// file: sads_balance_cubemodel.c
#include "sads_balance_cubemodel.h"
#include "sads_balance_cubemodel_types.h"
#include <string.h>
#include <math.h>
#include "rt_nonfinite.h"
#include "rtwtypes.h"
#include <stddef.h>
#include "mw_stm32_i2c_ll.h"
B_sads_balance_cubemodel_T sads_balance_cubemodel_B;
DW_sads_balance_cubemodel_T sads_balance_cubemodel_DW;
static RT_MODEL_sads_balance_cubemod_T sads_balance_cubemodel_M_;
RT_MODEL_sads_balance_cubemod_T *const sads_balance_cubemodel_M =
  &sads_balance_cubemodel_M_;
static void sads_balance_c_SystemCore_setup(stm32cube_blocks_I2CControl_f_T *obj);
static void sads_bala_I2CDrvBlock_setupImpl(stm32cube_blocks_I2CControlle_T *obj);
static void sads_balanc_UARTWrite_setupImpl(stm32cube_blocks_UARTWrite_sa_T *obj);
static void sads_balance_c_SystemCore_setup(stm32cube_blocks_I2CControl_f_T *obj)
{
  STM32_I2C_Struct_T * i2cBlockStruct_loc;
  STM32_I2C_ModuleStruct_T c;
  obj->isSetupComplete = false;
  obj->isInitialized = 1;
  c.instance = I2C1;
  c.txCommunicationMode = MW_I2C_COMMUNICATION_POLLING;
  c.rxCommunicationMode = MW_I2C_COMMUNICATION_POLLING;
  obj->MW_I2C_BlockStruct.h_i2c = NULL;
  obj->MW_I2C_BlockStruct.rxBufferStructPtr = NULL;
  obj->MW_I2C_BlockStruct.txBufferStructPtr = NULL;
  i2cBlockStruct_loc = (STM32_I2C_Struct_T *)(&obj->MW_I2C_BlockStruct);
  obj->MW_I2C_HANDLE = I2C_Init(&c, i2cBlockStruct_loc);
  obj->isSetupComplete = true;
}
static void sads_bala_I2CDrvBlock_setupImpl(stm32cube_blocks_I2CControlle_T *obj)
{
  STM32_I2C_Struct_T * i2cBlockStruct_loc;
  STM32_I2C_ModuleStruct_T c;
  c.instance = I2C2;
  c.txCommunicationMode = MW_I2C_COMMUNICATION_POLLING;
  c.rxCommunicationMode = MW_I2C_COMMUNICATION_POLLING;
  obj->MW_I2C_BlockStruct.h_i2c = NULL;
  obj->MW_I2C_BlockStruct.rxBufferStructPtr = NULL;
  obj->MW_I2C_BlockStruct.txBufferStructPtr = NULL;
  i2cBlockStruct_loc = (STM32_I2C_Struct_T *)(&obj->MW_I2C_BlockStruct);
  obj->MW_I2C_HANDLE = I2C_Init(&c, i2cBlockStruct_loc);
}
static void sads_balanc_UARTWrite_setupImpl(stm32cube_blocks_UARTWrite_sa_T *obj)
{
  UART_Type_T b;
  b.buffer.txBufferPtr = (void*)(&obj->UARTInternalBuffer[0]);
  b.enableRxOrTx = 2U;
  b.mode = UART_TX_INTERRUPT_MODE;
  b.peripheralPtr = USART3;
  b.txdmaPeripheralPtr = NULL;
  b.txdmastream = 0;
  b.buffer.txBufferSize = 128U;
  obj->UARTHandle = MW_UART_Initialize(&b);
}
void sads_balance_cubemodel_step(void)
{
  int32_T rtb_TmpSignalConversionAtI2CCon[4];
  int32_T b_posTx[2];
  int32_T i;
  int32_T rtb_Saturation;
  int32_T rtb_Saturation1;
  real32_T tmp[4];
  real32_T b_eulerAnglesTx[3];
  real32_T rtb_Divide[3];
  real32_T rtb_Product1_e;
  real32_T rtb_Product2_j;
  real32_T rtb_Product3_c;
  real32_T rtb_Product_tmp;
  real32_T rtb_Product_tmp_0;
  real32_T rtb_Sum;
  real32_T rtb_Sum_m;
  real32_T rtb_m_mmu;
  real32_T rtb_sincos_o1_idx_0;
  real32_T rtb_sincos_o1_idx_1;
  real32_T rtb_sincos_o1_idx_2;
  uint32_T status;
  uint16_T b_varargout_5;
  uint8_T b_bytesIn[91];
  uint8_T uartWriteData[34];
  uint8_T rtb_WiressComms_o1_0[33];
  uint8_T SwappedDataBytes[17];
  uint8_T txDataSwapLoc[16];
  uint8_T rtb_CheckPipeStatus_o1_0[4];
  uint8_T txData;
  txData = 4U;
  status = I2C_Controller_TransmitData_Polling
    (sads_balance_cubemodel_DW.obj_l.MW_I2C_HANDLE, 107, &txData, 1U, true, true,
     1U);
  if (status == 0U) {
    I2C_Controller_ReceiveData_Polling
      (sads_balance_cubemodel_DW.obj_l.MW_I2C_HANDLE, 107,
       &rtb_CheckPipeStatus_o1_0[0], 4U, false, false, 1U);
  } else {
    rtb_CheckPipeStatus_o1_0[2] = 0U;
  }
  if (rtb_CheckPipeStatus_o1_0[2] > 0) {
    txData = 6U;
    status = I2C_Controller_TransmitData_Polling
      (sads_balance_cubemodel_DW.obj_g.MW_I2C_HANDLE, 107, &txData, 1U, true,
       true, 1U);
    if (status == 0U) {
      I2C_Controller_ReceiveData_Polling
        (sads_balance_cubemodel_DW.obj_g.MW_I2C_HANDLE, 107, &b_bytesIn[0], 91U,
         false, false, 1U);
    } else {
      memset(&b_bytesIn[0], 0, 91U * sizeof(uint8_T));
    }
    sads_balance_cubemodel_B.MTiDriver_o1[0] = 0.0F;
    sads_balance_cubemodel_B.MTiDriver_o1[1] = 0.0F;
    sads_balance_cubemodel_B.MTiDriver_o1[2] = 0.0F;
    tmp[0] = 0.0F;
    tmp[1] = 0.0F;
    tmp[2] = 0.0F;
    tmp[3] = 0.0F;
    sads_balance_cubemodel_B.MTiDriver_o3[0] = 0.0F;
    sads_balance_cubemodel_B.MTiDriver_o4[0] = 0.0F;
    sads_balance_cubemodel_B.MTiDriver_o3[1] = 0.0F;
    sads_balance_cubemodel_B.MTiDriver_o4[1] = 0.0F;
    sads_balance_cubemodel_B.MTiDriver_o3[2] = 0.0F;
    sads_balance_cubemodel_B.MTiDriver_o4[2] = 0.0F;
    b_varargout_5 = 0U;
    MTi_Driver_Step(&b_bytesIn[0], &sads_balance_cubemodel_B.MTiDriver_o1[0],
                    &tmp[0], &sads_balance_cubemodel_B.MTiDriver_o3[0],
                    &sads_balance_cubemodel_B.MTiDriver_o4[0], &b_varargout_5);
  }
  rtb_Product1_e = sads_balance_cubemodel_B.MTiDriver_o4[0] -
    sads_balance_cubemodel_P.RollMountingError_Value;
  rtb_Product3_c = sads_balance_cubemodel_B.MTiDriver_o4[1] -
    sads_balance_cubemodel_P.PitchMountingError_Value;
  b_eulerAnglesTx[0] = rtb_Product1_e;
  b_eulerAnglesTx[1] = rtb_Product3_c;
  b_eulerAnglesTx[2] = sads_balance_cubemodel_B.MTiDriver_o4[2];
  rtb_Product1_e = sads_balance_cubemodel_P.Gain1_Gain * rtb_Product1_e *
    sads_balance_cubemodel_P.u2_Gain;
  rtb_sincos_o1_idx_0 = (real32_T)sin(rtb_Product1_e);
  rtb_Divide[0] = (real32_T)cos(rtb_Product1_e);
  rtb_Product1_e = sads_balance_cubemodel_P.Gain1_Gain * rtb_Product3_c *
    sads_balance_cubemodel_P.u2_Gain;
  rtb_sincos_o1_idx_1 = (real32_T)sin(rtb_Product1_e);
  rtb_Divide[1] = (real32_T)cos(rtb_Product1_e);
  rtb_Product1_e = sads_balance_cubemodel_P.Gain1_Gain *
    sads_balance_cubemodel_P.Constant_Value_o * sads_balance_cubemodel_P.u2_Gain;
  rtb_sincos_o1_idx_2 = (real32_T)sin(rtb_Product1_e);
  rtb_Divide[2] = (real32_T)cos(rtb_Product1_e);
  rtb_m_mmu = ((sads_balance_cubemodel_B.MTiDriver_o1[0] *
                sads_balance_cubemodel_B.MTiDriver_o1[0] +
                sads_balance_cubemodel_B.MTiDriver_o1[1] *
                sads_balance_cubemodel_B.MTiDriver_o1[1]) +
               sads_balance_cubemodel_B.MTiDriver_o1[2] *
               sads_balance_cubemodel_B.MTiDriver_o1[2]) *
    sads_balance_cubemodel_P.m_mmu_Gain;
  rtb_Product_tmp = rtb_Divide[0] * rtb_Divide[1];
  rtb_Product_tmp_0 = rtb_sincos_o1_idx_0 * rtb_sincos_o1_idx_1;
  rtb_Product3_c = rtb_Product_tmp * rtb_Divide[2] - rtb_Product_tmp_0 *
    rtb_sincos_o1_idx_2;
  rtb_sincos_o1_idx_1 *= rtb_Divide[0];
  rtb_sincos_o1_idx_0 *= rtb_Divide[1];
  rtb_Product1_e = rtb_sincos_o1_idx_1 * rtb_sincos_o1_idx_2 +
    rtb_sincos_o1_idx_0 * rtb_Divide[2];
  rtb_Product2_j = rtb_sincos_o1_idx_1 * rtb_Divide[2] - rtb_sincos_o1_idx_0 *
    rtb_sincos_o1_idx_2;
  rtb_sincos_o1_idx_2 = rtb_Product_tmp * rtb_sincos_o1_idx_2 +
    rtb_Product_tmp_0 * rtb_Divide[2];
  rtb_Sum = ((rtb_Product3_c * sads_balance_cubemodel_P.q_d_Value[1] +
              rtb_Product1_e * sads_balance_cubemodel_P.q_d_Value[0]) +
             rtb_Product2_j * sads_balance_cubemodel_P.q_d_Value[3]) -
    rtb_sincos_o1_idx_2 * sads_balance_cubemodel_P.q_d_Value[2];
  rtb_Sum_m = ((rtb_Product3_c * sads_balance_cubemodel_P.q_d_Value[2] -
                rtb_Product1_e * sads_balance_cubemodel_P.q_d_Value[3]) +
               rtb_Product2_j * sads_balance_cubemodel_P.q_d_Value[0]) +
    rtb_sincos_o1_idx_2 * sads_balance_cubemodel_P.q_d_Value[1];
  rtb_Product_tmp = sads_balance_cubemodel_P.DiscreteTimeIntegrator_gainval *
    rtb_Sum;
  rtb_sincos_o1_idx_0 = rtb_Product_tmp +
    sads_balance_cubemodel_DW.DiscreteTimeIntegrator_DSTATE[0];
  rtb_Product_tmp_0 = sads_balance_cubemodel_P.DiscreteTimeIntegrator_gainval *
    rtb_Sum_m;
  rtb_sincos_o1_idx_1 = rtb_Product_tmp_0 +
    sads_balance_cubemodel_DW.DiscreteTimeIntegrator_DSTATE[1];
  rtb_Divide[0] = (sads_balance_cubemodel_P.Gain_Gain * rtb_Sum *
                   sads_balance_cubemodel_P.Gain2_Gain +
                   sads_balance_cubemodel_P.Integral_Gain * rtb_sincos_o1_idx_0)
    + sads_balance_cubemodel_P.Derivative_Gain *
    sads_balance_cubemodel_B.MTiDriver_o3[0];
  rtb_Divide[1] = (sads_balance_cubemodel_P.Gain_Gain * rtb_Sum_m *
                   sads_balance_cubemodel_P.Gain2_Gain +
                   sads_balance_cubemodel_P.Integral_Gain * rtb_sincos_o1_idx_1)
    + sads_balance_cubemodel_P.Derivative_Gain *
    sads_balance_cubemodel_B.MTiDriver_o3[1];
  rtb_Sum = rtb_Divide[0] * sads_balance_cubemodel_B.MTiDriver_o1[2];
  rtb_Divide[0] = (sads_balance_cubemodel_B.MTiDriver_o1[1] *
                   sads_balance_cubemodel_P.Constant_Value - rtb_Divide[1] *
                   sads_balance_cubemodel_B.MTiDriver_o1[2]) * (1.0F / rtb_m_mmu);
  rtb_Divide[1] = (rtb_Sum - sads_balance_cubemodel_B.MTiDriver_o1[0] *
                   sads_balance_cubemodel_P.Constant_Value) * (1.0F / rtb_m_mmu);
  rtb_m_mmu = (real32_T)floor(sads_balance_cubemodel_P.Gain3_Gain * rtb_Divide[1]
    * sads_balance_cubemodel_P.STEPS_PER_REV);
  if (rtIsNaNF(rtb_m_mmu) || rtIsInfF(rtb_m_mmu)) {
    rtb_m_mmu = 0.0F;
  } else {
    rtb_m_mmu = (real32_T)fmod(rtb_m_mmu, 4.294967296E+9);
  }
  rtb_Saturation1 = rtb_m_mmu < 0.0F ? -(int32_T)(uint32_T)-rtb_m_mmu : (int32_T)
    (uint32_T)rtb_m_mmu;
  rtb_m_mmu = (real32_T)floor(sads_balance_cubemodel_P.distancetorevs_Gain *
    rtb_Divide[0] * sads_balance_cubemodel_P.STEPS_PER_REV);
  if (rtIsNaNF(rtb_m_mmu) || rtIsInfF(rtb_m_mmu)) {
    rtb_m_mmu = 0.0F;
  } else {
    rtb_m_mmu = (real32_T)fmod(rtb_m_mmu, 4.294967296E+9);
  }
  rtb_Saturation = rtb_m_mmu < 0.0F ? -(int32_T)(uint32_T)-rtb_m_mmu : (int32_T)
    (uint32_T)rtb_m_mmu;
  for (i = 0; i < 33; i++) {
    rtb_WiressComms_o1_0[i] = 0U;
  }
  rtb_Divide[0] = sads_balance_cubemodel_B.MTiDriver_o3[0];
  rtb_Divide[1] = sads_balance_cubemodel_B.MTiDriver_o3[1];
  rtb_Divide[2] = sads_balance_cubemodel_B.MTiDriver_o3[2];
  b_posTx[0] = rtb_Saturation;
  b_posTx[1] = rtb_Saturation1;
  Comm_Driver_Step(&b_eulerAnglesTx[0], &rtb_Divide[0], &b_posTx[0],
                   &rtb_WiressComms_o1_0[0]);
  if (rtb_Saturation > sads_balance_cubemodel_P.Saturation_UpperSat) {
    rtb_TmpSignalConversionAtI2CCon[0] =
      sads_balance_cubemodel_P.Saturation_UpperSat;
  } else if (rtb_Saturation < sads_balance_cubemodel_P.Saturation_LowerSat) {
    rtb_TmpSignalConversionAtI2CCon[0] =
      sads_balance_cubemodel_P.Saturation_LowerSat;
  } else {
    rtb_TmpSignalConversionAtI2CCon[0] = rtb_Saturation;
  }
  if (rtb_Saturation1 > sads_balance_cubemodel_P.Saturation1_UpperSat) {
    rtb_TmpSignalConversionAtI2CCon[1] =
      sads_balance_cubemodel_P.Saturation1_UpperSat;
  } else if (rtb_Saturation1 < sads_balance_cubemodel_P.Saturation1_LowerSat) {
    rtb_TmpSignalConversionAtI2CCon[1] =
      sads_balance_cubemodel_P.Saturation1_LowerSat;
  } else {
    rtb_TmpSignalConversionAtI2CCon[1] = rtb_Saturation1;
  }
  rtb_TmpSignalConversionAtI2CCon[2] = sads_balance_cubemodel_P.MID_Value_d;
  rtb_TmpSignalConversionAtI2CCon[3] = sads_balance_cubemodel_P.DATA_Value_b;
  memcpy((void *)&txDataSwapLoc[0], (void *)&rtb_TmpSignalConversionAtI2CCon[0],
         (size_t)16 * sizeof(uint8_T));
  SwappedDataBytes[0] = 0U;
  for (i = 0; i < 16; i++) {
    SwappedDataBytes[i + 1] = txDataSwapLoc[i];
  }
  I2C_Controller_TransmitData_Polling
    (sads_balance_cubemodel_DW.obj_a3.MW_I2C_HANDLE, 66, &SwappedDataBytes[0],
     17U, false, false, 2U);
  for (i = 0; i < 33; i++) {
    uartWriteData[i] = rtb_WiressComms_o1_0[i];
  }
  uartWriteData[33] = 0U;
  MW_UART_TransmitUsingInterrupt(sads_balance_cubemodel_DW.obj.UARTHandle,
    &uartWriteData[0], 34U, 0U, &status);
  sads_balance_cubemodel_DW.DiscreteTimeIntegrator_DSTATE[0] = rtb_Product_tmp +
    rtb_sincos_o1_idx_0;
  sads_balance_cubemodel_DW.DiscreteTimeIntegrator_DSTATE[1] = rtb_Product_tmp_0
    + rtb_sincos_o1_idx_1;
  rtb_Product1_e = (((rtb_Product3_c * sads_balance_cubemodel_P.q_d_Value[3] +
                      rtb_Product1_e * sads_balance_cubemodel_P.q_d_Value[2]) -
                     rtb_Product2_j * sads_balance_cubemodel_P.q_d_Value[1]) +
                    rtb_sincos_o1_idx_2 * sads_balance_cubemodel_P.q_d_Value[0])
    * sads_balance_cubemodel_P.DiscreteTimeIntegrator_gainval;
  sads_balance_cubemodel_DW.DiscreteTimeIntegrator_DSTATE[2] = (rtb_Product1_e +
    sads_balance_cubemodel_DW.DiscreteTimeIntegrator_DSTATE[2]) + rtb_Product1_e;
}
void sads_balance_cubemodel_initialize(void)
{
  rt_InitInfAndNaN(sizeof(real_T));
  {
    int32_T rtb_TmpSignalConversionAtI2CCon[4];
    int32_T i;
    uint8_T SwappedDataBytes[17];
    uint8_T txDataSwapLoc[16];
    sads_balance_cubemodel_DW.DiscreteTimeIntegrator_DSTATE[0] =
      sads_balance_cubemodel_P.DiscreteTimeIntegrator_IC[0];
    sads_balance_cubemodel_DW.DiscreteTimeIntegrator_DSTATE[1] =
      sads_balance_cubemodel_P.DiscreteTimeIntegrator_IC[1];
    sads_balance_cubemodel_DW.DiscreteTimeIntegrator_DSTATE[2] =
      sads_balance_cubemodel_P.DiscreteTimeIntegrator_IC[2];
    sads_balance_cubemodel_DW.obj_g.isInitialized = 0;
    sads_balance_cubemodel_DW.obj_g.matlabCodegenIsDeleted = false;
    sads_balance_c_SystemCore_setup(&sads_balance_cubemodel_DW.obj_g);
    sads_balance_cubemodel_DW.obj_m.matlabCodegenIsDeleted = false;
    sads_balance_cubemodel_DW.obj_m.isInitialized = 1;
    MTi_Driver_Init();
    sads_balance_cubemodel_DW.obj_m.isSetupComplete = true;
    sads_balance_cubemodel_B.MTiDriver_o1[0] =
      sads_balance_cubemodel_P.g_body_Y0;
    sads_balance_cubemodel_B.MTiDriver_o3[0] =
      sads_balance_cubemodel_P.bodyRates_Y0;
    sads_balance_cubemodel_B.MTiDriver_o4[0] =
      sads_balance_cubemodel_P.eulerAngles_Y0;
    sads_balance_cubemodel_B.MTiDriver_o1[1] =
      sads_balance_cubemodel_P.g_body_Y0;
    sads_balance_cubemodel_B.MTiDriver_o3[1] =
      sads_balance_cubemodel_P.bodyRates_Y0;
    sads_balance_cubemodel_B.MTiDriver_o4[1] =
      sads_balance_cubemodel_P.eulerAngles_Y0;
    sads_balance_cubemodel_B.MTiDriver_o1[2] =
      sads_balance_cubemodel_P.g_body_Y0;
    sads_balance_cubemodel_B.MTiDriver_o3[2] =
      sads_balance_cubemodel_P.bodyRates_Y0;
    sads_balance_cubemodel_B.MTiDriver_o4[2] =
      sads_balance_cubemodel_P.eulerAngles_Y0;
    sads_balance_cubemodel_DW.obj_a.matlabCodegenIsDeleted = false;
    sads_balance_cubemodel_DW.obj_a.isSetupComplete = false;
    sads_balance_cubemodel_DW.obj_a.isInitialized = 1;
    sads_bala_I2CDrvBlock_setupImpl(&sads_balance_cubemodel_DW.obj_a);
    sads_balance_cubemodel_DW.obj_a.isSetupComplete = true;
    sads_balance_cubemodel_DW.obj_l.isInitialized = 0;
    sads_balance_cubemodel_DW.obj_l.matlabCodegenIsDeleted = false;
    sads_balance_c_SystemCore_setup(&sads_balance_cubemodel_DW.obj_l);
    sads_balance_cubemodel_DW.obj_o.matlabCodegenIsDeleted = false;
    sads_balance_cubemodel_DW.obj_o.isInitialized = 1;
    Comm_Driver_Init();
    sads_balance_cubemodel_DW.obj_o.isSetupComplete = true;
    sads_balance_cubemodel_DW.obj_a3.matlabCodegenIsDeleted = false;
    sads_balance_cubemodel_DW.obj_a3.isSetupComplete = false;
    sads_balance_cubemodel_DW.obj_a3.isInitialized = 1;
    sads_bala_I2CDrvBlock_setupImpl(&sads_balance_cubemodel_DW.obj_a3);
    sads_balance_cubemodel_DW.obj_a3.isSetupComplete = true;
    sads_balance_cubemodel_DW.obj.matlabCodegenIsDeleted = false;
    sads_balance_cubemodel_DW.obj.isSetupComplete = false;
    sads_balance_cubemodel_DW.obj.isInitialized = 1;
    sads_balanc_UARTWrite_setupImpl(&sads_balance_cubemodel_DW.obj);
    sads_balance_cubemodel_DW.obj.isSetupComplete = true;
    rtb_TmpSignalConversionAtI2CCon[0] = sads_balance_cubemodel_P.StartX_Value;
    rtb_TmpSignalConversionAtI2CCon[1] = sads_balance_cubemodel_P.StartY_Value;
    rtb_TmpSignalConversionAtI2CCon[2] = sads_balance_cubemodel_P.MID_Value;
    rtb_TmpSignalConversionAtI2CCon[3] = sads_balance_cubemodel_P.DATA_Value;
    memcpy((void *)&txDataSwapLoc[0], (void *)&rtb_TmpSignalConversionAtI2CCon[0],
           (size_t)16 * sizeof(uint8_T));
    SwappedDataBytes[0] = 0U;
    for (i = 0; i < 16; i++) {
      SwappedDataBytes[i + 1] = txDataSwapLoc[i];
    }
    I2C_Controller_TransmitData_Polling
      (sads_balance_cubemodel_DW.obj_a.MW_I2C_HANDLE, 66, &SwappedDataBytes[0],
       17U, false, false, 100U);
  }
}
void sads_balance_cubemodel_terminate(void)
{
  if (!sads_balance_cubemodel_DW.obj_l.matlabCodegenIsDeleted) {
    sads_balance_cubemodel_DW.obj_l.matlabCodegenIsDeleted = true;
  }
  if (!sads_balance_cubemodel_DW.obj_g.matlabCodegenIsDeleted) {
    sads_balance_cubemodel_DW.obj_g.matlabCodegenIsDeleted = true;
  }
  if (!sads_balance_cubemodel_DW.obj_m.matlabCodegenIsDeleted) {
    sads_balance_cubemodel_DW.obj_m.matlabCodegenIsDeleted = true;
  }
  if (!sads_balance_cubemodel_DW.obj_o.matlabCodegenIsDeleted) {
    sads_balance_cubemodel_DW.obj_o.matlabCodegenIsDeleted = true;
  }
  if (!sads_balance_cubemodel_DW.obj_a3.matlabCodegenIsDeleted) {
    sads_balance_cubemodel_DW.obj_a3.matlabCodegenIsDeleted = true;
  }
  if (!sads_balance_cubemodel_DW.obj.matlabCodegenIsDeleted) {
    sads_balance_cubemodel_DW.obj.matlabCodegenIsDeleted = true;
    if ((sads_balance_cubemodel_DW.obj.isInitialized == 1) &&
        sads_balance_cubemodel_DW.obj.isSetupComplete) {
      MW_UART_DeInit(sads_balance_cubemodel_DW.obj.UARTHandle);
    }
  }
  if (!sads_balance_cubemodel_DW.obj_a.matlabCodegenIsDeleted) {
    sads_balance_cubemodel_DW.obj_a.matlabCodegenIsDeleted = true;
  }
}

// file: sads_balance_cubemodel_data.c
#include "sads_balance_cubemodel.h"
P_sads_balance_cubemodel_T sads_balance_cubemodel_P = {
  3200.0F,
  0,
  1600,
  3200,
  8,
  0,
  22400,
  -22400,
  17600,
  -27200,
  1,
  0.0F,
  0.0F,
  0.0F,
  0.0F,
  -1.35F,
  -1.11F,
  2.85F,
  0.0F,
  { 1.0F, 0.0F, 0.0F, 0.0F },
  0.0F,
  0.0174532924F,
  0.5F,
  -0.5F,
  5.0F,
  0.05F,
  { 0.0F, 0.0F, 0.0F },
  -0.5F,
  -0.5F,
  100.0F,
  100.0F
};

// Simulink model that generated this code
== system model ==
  USARTWrite#1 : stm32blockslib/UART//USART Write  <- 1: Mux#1
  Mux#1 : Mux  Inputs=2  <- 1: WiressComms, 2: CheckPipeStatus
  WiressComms : MATLABSystem  <- 1: From#1, 2: Subsystem#1/3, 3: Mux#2
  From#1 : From
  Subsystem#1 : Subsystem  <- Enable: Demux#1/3
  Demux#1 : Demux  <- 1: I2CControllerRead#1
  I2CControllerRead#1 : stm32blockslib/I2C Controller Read
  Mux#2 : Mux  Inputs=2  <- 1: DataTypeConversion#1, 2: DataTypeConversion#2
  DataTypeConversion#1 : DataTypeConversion  <- 1: Gain#1
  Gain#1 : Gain  Gain=STEPS_PER_REV  <- 1: distancetorevs
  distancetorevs : Gain  Gain=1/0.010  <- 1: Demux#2
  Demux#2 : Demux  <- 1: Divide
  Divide : Product  Inputs=/*  <- 1: m_mmu, 2: CrossProduct#1
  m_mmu : Gain  Gain=2.85  <- 1: DotProduct#1
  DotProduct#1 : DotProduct  <- 1: Subsystem#1, 2: Subsystem#1
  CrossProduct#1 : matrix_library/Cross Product  <- 1: Subsystem#1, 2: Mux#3
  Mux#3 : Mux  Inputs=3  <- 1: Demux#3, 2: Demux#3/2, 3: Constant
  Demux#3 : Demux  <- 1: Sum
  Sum : Sum  Inputs=+++  <- 1: Gain2, 2: Integral, 3: Derivative
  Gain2 : Gain  Gain=5  <- 1: Gain
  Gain : Gain  Gain=-0.5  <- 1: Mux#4
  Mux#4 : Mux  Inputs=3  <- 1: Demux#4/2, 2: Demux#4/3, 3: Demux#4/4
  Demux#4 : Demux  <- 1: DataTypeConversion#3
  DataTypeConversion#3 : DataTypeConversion  <- 1: QuaternionMultiplication#1
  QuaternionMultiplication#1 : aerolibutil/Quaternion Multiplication  <- 1: DataTypeConversion#4, 2: q_d
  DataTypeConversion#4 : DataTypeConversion  <- 1: RotationAnglestoQuaternions#1
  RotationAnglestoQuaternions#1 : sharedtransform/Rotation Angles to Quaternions  <- 1: DegreestoRadians#1
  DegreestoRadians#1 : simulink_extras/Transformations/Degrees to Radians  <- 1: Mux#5
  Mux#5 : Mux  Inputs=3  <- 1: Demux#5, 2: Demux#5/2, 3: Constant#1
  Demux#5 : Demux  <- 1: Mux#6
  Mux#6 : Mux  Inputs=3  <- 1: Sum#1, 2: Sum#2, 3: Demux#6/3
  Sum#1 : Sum  Inputs=+-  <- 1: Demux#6, 2: RollMountingError
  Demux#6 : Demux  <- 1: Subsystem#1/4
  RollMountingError : Constant  Value=-1.35
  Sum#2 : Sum  Inputs=+-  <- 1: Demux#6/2, 2: PitchMountingError
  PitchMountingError : Constant  Value=-1.11
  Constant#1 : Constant  Value=0
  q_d : Constant  Value=[1 0 0 0]'
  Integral : Gain  Gain=-0.5  <- 1: DiscreteTimeIntegrator
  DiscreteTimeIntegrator : DiscreteIntegrator  IntegratorMethod=Integration: Trapezoidal  InitialCondition=[0,0,0]'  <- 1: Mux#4
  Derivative : Gain  Gain=-0.5  <- 1: Subsystem#1/3
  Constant : Constant  Value=0
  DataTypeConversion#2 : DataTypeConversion  <- 1: Gain1
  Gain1 : Gain  Gain=STEPS_PER_REV  <- 1: Gain3
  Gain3 : Gain  Gain=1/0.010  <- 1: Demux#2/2
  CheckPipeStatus : stm32blockslib/I2C Controller Read
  Goto#1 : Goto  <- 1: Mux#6
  Saturation : Saturate  UpperLimit=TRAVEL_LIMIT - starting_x  LowerLimit=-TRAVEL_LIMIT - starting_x  <- 1: DataTypeConversion#1
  Saturation1 : Saturate  UpperLimit=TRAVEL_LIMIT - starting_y  LowerLimit=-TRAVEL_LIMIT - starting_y  <- 1: DataTypeConversion#2
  DATA : Constant  Value=0
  MID : Constant
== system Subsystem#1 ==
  EnablePort#1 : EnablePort
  g_body : Outport  <- 1: MTiDriver
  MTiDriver : MATLABSystem  <- 1: I2CControllerRead#2
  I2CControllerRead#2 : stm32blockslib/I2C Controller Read
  Outport#1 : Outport  <- 1: MTiDriver/2
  bodyRates : Outport  <- 1: MTiDriver/3
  eulerAngles : Outport  <- 1: MTiDriver/4
